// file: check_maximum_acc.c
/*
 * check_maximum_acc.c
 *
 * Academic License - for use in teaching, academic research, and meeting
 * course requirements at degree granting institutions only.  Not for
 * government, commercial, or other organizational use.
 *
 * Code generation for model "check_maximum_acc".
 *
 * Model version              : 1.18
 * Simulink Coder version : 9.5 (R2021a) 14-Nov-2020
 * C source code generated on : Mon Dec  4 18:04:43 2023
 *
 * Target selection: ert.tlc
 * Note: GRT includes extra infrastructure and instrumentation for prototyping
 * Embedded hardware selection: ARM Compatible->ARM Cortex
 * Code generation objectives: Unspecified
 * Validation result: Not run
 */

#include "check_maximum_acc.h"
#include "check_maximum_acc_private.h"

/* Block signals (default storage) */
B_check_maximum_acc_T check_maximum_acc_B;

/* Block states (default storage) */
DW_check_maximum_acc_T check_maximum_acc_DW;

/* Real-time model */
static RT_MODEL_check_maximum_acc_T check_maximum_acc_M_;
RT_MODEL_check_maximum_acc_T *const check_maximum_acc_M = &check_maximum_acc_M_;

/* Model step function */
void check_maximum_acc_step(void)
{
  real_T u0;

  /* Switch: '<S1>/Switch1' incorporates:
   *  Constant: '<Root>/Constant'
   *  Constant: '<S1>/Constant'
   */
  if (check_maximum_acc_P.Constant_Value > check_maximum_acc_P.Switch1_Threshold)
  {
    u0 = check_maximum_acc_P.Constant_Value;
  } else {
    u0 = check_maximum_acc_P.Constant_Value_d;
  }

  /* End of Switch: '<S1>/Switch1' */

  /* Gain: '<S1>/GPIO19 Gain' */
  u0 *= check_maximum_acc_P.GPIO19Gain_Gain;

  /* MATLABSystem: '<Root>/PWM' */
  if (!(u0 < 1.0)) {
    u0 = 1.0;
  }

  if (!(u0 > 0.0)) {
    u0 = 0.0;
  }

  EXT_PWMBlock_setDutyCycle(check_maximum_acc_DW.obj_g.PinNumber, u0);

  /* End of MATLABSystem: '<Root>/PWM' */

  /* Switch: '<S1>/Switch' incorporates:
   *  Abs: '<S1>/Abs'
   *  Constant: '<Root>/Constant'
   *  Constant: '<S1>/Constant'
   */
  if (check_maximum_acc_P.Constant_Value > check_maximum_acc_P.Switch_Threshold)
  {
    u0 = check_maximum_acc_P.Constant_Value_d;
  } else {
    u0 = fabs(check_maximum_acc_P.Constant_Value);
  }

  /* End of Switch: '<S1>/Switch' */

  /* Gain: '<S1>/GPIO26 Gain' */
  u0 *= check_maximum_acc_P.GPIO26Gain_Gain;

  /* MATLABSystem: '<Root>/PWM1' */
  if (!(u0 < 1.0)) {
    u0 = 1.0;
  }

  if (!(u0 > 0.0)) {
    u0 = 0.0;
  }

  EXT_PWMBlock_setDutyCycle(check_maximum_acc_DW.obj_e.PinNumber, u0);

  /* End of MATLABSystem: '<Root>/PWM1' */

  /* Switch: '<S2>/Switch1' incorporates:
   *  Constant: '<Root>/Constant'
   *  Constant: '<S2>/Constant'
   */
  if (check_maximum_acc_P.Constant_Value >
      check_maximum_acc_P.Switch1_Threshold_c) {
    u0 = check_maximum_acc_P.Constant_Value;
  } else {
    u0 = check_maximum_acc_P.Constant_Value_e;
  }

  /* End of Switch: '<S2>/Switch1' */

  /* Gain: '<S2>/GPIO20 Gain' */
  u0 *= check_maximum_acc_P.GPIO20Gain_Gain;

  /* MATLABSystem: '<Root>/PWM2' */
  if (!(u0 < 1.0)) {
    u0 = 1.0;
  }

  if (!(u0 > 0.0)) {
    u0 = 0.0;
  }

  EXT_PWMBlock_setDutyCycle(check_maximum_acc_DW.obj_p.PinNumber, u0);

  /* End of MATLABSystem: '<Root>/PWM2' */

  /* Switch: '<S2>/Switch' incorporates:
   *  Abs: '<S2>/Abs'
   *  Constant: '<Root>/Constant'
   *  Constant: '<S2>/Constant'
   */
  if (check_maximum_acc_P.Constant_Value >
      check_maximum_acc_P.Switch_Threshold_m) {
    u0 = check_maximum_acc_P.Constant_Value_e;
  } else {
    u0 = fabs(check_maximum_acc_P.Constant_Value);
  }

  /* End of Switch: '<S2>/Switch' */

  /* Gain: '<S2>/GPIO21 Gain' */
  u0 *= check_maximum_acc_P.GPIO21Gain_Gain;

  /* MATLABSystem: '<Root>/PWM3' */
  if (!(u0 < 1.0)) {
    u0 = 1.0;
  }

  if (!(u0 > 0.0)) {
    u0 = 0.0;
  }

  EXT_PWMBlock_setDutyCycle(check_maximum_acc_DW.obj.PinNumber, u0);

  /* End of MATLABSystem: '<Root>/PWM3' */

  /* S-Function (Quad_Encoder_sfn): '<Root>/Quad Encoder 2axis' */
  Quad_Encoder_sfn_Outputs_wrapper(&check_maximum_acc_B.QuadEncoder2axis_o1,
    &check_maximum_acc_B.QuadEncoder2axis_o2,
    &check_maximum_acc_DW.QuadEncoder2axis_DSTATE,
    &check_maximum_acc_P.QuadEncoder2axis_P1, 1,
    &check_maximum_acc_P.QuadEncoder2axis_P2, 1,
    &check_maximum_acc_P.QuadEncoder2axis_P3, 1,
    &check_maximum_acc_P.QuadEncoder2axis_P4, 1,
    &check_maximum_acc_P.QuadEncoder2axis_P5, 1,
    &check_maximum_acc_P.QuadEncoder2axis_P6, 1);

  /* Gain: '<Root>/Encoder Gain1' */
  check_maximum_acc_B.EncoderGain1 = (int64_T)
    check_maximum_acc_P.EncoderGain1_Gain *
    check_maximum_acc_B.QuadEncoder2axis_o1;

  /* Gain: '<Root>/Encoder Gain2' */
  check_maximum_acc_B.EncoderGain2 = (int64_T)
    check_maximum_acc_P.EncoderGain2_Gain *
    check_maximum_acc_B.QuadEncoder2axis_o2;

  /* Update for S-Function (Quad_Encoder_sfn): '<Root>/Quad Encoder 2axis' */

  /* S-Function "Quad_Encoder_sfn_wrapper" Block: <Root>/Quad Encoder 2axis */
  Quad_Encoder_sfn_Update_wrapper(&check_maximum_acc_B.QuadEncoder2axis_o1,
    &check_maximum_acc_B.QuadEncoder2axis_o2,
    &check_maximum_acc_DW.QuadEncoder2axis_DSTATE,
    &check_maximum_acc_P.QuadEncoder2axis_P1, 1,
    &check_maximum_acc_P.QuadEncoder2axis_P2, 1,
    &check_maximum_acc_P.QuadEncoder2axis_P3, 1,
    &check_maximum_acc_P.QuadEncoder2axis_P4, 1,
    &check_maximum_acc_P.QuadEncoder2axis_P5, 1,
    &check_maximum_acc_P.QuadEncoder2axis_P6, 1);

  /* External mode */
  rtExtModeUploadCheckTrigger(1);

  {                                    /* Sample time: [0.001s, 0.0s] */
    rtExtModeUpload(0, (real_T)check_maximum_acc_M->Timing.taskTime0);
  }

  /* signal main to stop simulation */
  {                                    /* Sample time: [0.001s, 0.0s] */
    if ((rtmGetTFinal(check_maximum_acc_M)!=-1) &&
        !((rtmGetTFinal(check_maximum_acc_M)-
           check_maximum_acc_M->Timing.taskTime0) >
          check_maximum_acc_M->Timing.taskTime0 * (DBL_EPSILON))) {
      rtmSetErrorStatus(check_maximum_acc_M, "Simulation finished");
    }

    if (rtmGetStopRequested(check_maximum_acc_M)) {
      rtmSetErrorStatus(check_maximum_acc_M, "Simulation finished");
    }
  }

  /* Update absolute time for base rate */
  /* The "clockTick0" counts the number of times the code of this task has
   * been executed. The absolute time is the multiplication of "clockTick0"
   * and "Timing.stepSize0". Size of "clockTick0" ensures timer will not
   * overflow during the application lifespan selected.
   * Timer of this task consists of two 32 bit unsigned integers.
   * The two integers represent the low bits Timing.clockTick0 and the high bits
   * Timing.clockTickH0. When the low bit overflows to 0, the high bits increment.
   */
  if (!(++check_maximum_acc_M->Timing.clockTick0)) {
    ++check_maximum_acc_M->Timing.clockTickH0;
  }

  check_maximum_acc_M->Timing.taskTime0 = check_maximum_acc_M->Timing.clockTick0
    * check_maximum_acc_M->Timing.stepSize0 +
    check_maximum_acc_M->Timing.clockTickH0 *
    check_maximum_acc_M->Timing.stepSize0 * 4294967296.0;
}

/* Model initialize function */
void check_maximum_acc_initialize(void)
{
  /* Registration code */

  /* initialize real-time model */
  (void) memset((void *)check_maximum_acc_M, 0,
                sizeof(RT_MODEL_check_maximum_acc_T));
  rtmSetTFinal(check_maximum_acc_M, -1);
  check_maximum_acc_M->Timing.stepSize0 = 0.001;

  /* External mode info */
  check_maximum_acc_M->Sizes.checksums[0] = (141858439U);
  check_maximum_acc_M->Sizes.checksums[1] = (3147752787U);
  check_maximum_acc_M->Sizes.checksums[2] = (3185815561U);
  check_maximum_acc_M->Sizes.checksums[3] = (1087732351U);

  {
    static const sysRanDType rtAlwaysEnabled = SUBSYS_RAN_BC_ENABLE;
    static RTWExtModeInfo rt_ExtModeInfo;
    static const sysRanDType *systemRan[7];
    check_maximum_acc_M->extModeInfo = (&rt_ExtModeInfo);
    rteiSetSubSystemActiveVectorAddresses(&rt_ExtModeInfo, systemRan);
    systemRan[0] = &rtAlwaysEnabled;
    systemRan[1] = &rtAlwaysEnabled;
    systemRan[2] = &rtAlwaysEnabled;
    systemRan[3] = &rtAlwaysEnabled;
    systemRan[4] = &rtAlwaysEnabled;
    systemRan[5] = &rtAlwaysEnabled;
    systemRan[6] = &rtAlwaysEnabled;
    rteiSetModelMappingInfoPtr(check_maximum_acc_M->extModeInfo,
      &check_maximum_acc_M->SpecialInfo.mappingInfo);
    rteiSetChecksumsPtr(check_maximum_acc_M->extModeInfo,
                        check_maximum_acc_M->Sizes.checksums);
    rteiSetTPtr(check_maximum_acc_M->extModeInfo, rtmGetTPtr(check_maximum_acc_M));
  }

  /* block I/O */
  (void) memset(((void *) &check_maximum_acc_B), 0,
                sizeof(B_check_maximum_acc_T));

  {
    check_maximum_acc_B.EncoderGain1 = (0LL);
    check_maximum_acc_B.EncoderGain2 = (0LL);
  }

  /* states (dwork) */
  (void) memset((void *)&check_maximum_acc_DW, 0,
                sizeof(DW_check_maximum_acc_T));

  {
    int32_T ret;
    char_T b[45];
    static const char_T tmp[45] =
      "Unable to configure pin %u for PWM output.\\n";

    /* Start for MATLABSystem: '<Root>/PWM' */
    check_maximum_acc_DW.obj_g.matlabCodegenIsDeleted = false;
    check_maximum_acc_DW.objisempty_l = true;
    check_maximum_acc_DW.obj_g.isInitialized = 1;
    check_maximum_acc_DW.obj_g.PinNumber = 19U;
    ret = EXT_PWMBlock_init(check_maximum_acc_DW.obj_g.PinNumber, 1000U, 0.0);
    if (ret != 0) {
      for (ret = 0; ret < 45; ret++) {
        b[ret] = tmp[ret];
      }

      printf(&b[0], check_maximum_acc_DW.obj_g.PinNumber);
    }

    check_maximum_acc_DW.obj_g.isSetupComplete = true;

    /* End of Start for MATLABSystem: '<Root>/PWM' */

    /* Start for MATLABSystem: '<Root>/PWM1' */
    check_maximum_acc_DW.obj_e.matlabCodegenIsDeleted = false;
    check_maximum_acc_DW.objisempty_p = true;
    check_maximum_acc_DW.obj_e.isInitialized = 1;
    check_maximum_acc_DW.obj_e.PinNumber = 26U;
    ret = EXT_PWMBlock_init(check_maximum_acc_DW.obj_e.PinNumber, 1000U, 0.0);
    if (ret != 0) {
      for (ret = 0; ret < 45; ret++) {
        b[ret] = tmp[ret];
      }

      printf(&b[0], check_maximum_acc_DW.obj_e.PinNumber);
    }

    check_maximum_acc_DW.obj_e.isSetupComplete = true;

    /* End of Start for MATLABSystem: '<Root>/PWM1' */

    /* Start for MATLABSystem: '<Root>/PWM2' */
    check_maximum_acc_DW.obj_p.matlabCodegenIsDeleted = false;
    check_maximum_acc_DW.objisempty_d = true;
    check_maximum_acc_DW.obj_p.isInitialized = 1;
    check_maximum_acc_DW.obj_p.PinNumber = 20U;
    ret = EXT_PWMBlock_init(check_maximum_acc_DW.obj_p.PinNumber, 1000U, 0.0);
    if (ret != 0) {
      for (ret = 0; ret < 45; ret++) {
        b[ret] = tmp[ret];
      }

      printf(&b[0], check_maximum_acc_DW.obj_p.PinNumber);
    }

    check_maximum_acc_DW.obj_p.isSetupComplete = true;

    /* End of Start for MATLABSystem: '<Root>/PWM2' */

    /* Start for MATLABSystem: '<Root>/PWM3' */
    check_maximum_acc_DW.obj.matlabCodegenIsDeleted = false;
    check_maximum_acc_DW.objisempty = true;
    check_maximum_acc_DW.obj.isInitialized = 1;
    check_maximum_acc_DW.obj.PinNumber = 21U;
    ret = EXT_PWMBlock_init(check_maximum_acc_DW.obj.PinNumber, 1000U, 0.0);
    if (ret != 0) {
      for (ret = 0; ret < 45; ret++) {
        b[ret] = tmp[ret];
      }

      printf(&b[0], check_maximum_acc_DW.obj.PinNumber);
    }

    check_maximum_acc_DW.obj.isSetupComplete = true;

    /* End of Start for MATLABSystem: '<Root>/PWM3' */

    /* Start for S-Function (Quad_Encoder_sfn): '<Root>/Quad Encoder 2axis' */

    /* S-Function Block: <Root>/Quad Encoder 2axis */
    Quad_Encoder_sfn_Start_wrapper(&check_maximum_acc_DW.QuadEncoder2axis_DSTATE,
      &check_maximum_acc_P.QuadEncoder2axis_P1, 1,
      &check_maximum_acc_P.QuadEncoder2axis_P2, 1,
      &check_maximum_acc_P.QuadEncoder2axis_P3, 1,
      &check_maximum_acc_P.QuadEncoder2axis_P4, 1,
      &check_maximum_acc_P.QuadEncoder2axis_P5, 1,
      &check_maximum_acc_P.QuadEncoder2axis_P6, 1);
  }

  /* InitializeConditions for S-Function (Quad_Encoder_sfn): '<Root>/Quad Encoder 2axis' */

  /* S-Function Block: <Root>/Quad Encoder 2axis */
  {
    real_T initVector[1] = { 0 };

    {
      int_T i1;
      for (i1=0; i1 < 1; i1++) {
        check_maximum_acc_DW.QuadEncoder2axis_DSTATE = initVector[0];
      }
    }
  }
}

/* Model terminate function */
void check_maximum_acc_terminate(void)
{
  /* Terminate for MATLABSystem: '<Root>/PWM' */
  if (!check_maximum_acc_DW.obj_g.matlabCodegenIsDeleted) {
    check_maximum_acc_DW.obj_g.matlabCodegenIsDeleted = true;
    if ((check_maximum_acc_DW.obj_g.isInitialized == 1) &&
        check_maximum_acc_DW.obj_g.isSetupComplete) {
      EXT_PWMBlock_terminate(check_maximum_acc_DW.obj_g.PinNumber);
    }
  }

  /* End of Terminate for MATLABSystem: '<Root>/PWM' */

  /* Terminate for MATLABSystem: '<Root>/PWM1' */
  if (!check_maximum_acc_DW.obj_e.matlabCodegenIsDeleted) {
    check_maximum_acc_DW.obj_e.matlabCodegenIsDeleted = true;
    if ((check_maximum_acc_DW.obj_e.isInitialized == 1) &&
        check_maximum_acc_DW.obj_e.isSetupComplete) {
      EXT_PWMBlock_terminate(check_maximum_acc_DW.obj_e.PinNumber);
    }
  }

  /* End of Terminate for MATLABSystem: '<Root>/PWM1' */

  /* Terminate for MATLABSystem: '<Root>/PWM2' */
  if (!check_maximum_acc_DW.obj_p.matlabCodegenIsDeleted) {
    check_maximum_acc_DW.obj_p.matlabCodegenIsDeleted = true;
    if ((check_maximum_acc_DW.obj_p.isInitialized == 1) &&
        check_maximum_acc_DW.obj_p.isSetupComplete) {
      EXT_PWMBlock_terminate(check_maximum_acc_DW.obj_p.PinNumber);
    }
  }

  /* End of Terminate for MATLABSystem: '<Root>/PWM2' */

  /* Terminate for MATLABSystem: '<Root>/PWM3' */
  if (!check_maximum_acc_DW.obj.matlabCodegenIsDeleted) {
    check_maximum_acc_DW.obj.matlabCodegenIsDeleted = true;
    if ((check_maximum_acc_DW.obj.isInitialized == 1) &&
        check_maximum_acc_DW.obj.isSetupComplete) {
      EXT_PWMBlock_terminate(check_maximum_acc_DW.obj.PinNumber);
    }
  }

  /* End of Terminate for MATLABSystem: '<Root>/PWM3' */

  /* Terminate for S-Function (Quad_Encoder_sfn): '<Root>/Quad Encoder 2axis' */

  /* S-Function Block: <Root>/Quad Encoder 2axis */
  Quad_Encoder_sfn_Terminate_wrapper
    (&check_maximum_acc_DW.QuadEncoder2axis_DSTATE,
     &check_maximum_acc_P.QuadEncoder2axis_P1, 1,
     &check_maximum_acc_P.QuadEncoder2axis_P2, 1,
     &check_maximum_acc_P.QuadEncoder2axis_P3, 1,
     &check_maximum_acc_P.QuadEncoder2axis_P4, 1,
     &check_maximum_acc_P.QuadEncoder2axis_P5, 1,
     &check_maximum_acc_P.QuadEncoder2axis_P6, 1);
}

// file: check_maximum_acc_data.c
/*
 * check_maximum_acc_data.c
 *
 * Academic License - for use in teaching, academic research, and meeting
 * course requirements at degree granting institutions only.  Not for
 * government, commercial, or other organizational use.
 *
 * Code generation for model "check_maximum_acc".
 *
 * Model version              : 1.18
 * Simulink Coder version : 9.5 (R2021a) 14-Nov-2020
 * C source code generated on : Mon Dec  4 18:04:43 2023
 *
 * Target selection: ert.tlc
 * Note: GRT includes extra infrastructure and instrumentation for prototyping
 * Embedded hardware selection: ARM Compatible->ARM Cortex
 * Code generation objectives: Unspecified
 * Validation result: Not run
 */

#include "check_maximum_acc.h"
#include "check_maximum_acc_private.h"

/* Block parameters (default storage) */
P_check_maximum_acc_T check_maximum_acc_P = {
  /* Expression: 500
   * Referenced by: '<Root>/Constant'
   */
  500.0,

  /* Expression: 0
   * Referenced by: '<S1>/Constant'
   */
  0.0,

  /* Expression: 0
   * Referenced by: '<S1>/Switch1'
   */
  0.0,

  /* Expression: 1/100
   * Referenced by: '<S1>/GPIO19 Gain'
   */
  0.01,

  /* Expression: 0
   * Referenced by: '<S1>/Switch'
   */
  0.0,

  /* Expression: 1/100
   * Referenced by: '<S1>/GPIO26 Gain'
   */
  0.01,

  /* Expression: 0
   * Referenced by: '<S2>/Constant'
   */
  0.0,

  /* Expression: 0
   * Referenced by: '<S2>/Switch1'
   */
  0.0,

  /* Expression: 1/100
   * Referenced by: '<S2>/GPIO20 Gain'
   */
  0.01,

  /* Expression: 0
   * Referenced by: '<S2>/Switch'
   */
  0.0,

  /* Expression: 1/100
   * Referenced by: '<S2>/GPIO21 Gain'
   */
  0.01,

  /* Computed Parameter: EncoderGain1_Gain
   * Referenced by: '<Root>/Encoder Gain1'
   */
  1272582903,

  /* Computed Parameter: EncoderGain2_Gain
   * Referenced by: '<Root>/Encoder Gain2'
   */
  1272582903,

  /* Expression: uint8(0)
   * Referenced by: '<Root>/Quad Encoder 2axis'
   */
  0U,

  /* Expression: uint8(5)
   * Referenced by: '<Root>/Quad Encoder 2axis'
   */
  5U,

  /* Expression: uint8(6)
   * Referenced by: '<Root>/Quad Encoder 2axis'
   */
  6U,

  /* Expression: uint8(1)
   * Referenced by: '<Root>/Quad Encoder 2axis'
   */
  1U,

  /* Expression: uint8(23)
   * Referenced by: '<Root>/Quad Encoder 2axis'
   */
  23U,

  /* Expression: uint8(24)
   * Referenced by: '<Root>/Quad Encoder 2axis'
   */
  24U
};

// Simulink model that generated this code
simulink model "check_maximum_acc"  (R2021a)
settings: Solver=FixedStepAuto  StartTime=0.0  StopTime=inf  FixedStep=0.001  RelTol=1e-3  EnableMultiTasking=on
StopFcn:
  | mypi=raspi();
  | writeDigitalPin(mypi,19,0);
  | writeDigitalPin(mypi,26,0);
  | writeDigitalPin(mypi,20,0);
  | writeDigitalPin(mypi,21,0);
  | clear mypi;
libraries: raspberrypiBasiclib x4

== system check_maximum_acc ==
  note: Encoder Position (To Workspace)
  Constant : Constant  Value=500
  Encoder Gain1 : Gain  Gain=1/216
  Encoder Gain2 : Gain  Gain=1/216
  Motor Subsystem : Subsystem
  Motor Subsystem1 : Subsystem
  PWM : raspberrypiBasiclib/PWM  board=Pi 4 Model B  Pin_=19  Frequency=1000  blockPlatform=Raspberry Pi
  PWM1 : raspberrypiBasiclib/PWM  board=Pi 4 Model B  Pin_=26  Frequency=1000  blockPlatform=Raspberry Pi
  PWM2 : raspberrypiBasiclib/PWM  board=Pi 4 Model B  Pin_=20  Frequency=1000  blockPlatform=Raspberry Pi
  PWM3 : raspberrypiBasiclib/PWM  board=Pi 4 Model B  Pin_=21  Frequency=1000  blockPlatform=Raspberry Pi
  Quad Encoder 2axis : S-Function  InitFcn=try, set_param(gcb,'FunctionName','Quad_Encoder_sfn'), end  FunctionName=Quad_Encoder_sfn  Parameters=uint8(0),uint8(5),uint8(6),uint8(1),uint8(23),uint8(24)  SFunctionModules=Quad_Encoder_sfn_wrapper  SFunctionDeploymentMode=off  EnableBusSupport=off  mask(S-Function Builder){}
      mask init:
      | val = [[.9  0.75 0.75 1 1 .9 .9 1]',[1 1 0.75 0.75 .9 .9 1 .9]'];try , sys = get_param(gcb,'SfunBuilderFcnName');if isempty(sys), sys = get_param(gcb,'FunctionName'); end,catch, sys = get_param(gcb,'FunctionName'); end
  To Workspace : ToWorkspace  VariableName=controled_position  SaveFormat=Structure With Time  SampleTime=0.001
  To Workspace1 : ToWorkspace  VariableName=simout  SaveFormat=Timeseries  SampleTime=-1
  To Workspace2 : ToWorkspace  VariableName=simout1  SaveFormat=Timeseries  SampleTime=-1
  wires:
  Quad Encoder 2axis/1 -> Encoder Gain1/1
  Quad Encoder 2axis/2 -> Encoder Gain2/1
  Motor Subsystem/1(Out1) -> PWM/1
  Motor Subsystem/2(Out2) -> PWM1/1
  Motor Subsystem1/2(Out2) -> PWM3/1
  Motor Subsystem1/1(Out1) -> PWM2/1
  Constant/1 -> Motor Subsystem1/1(In1), Motor Subsystem/1(In1)
  Encoder Gain1/1 -> To Workspace1/1
  Encoder Gain2/1 -> To Workspace2/1

== system check_maximum_acc/Motor Subsystem ==
  In1 : Inport
  Abs : Abs
  Constant : Constant  Value=0
  GPIO19 Gain : Gain  Gain=1/100
  GPIO26 Gain : Gain  Gain=1/100
  Switch : Switch  Criteria=u2 > Threshold
  Switch1 : Switch  Criteria=u2 > Threshold
  Out1 : Outport
  Out2 : Outport  Port=2
  wires:
  Switch/1 -> GPIO26 Gain/1
  Abs/1 -> Switch/3
  Switch1/1 -> GPIO19 Gain/1
  In1/1 -> Abs/1, Switch/2, Switch1/1, Switch1/2
  Constant/1 -> Switch/1, Switch1/3
  GPIO26 Gain/1 -> Out2/1
  GPIO19 Gain/1 -> Out1/1

== system check_maximum_acc/Motor Subsystem1 ==
  In1 : Inport
  Abs : Abs
  Constant : Constant  Value=0
  GPIO20 Gain : Gain  Gain=1/100
  GPIO21 Gain : Gain  Gain=1/100
  Switch : Switch  Criteria=u2 > Threshold
  Switch1 : Switch  Criteria=u2 > Threshold
  Out1 : Outport
  Out2 : Outport  Port=2
  wires:
  Switch/1 -> GPIO21 Gain/1
  Abs/1 -> Switch/3
  Switch1/1 -> GPIO20 Gain/1
  In1/1 -> Abs/1, Switch/2, Switch1/1, Switch1/2
  Constant/1 -> Switch/1, Switch1/3
  GPIO21 Gain/1 -> Out2/1
  GPIO20 Gain/1 -> Out1/1
